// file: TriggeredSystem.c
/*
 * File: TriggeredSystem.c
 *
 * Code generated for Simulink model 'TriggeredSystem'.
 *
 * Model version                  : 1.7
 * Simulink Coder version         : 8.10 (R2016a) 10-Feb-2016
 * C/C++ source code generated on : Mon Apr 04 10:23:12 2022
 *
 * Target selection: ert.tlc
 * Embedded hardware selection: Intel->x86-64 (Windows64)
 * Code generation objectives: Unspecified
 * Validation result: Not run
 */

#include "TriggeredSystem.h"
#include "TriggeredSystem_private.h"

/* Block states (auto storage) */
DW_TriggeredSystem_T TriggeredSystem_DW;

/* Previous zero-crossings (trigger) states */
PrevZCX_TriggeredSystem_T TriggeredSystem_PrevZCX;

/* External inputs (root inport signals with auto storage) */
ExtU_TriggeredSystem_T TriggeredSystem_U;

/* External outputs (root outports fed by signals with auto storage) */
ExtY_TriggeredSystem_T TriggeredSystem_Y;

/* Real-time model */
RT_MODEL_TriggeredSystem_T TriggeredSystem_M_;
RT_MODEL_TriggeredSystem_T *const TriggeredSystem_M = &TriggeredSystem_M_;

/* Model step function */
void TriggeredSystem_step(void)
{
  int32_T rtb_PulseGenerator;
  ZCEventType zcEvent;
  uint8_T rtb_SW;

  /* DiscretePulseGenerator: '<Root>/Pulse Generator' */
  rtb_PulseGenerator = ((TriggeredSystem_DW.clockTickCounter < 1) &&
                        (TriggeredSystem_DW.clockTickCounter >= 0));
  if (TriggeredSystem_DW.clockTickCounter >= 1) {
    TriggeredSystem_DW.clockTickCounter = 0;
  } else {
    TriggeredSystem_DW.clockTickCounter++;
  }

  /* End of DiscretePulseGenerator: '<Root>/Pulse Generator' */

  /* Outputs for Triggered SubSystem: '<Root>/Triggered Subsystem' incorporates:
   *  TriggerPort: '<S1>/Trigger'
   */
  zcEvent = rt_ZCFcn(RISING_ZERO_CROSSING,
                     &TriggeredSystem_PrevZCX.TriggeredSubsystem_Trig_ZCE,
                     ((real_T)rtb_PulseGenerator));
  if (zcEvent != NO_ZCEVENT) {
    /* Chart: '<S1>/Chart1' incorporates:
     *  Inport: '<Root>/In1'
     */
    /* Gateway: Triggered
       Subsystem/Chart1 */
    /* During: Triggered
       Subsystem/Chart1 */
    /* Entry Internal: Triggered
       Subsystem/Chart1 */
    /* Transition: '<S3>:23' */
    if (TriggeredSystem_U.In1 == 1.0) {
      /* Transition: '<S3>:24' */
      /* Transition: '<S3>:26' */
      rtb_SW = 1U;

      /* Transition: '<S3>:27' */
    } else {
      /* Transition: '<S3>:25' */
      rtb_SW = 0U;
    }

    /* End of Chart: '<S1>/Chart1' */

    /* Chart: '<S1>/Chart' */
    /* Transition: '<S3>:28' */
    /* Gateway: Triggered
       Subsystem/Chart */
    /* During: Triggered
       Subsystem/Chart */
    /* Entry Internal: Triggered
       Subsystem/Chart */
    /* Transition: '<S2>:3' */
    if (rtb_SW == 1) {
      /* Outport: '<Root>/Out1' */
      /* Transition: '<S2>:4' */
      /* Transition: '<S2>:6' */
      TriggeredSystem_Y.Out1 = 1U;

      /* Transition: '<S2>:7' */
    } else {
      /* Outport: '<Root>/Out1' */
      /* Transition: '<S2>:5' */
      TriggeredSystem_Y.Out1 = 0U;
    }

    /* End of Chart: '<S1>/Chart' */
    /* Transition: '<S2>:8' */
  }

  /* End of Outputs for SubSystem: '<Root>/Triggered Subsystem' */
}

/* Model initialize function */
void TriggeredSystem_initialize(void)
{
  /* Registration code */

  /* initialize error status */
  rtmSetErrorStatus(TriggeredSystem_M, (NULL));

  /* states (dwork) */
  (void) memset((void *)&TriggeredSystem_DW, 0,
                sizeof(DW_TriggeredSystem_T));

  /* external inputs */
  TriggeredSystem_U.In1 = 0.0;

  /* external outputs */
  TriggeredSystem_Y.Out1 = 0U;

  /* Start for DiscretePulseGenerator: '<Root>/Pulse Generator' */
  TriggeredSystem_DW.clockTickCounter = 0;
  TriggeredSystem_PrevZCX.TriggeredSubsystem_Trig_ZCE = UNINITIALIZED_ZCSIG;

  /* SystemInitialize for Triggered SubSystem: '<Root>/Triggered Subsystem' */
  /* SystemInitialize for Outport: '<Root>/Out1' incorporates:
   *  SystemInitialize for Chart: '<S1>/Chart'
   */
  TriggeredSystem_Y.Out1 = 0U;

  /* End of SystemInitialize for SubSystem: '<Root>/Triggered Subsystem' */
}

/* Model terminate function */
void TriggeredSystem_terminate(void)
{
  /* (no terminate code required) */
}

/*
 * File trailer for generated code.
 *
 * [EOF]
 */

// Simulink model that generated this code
simulink model "TriggeredSystem"  (R2016a)
settings: Solver=FixedStepDiscrete  StartTime=0.0  StopTime=0.03  RelTol=1e-3

== system TriggeredSystem ==
  In1 : Inport
  Display : Display
  Pulse Generator : DiscretePulseGenerator  PulseType=Time based  Period=0.005  PulseWidth=50
  Scope : Scope
  Triggered Subsystem : Subsystem  TreatAsAtomicUnit=on
  Out1 : Outport
  wires:
  Pulse Generator/1 -> Triggered Subsystem/Trigger
  Triggered Subsystem/1(Out1) -> Scope/1, Display/1, Out1/1
  In1/1 -> Triggered Subsystem/1(In1)

== system TriggeredSystem/Triggered Subsystem ==
  In1 : Inport
  Trigger : TriggerPort  VariantControl=Variant
  Chart : Stateflow chart  TreatAsAtomicUnit=on
  Chart1 : Stateflow chart  TreatAsAtomicUnit=on
  Out1 : Outport
  wires:
  Chart/1(led) -> Out1/1
  In1/1 -> Chart1/1(SWS)
  Chart1/1(SW) -> Chart/1(SW)

== stateflow chart TriggeredSystem/Triggered Subsystem/Chart1 ==
  (default) -> (junction 29)
  (junction 29) -> (junction 30) [order 1] : [SWS == 1]
  (junction 29) -> (junction 31) [order 2] : {SW = 0;}
  (junction 30) -> (junction 32) : {SW = 1;}
  (junction 32) -> (junction 31)
  (junction 31) -> (junction 33)
  data: SWS input; SW output uint8

== stateflow chart TriggeredSystem/Triggered Subsystem/Chart ==
  (default) -> (junction 9)
  (junction 9) -> (junction 10) [order 1] : [SW == 1]
  (junction 9) -> (junction 11) [order 2] : {led = uint8(0);}
  (junction 10) -> (junction 12) : {led = uint8(1);}
  (junction 12) -> (junction 11)
  (junction 11) -> (junction 13)
  data: led output uint8; SW input uint8
